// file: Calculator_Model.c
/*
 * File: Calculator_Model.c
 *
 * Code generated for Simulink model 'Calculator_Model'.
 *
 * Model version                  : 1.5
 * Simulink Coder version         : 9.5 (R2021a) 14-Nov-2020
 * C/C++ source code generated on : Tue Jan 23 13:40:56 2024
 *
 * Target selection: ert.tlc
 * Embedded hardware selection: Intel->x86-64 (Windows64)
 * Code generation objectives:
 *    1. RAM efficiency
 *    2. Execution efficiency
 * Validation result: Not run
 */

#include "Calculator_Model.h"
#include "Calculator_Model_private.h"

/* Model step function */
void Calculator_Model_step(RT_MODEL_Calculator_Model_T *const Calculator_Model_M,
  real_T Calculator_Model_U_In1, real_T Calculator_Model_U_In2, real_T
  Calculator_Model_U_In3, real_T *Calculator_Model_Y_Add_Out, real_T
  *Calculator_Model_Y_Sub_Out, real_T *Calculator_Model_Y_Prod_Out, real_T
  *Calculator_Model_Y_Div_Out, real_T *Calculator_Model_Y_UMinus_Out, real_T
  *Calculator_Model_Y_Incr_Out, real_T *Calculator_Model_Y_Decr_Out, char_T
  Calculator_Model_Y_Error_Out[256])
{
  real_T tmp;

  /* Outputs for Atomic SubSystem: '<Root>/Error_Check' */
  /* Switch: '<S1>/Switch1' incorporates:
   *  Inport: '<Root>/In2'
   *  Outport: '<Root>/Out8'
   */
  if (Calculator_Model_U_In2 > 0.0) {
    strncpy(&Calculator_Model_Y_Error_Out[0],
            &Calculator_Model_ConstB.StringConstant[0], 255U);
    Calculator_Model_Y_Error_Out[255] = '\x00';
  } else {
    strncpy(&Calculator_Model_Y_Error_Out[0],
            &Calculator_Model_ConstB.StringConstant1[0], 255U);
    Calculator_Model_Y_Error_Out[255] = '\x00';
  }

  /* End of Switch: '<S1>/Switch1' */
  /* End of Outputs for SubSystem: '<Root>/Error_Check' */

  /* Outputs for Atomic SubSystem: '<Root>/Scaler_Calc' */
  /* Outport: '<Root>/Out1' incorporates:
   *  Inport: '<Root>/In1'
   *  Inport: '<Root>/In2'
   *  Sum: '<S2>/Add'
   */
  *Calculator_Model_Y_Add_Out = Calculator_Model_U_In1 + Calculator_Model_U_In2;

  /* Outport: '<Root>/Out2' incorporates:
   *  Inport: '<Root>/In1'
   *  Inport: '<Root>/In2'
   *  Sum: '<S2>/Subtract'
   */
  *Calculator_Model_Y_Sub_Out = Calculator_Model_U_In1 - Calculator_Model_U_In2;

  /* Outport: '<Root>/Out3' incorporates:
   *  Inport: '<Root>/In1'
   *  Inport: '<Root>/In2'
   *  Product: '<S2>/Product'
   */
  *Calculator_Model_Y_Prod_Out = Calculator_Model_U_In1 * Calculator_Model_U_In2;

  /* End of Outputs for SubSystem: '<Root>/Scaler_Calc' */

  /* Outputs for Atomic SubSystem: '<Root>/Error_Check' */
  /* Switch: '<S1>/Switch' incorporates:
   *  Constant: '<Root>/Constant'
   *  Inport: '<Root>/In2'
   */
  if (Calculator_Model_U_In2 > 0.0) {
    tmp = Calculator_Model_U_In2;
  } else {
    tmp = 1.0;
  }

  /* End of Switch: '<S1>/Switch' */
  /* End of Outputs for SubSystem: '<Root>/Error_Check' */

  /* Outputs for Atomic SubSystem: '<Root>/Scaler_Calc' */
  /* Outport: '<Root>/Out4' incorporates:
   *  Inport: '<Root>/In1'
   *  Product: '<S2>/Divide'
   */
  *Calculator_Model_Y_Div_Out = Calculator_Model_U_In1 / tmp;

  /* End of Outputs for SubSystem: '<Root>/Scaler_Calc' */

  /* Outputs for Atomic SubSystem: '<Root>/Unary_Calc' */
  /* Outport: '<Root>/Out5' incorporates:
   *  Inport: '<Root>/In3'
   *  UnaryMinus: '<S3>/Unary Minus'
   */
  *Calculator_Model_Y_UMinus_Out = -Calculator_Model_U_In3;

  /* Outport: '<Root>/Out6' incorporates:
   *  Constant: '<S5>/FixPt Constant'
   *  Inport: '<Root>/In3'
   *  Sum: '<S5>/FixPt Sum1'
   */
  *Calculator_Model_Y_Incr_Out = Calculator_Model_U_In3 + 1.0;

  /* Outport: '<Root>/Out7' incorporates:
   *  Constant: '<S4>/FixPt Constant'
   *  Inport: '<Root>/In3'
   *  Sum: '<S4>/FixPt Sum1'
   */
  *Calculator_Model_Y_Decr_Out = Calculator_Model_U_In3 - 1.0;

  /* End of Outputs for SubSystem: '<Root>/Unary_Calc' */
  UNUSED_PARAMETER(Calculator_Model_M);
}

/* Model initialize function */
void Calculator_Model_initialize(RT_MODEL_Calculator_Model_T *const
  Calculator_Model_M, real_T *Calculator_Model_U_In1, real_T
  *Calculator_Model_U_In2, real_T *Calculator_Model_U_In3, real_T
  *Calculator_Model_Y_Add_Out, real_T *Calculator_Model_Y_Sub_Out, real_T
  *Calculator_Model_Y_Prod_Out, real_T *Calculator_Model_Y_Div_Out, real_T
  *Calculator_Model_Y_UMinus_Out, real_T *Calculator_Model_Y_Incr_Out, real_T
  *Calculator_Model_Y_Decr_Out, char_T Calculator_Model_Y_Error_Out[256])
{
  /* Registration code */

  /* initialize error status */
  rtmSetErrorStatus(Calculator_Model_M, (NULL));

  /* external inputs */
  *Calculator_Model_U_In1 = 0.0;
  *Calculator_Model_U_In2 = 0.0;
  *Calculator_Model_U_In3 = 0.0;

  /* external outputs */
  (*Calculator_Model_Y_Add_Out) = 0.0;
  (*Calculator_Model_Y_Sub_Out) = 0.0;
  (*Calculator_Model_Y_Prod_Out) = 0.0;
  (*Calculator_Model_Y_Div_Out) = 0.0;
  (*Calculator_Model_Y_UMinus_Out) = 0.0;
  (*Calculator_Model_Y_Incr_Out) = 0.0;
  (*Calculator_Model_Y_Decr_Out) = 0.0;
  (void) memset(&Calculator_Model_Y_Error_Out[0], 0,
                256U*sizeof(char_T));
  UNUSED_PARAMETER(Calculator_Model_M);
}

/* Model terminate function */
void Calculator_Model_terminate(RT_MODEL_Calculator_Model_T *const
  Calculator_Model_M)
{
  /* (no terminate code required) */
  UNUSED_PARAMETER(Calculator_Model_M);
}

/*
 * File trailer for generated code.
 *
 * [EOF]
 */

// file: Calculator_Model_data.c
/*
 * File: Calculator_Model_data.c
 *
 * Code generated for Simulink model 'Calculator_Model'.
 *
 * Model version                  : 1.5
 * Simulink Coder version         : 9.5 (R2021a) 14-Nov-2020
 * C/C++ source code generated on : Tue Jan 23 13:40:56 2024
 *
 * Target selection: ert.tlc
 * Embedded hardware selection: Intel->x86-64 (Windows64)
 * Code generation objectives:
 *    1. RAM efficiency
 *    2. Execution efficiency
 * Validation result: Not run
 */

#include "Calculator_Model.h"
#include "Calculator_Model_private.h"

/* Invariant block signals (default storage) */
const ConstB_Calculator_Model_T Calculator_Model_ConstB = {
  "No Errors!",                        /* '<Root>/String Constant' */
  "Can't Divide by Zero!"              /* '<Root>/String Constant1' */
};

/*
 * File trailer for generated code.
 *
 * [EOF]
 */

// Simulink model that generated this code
simulink model "Calculator_Model"  (R2021a)
settings: Solver=FixedStepDiscrete  StartTime=0.0  StopTime=10.0  RelTol=1e-3
libraries: simulink x2

== system Calculator_Model ==
  In1 : Inport  PortDimensions=1
  In2 : Inport  Port=2  PortDimensions=1
  In3 : Inport  Port=3  PortDimensions=1
  Constant : Constant
  Error_Check : Subsystem  TreatAsAtomicUnit=on
  Scaler_Calc : Subsystem  TreatAsAtomicUnit=on
  String Constant : StringConstant  String="\"No Errors!\""
  String Constant1 : StringConstant  String="\"Can't Divide by Zero!\""
  Unary_Calc : Subsystem  TreatAsAtomicUnit=on
  Out1 : Outport  SignalName=Add_Out
  Out2 : Outport  Port=2  SignalName=Sub_Out
  Out3 : Outport  Port=3  SignalName=Prod_Out
  Out4 : Outport  Port=4  SignalName=Div_Out
  Out5 : Outport  Port=5  SignalName=UMinus_Out
  Out6 : Outport  Port=6  SignalName=Incr_Out
  Out7 : Outport  Port=7  SignalName=Decr_Out
  Out8 : Outport  Port=8  SignalName=Error_Out
  wires:
  In1/1 -> [Num1]
  In3/1 -> [Num3]
  In2/1 -> [Num2]
  [Num1] -> Scaler_Calc/1(In1)
  [Num2] -> Scaler_Calc/2(In2)
  [Num1] -> Scaler_Calc/3(In3)
  [Num2] -> Scaler_Calc/4(In4)
  [Num1] -> Scaler_Calc/5(In5)
  [Num2] -> Scaler_Calc/6(In6)
  [Num1] -> Scaler_Calc/7(In7)
  Scaler_Calc/1(Out1) -> Out1/1
  Scaler_Calc/2(Out2) -> Out2/1
  Scaler_Calc/3(Out3) -> Out3/1
  Scaler_Calc/4(Out4) -> Out4/1
  [Num3] -> Unary_Calc/1(In1)
  [Num3] -> Unary_Calc/2(u)
  [Num3] -> Unary_Calc/3(u1)
  Unary_Calc/1(Out1) -> Out5/1
  Unary_Calc/2(y) -> Out6/1
  Unary_Calc/3(y1) -> Out7/1
  [Num2] -> Error_Check/1(In1)
  Constant/1 -> Error_Check/2(In2)
  String Constant/1 -> Error_Check/3(In3)
  String Constant1/1 -> Error_Check/4(In4)
  Error_Check/1(Out1) -> Scaler_Calc/8(In8)
  Error_Check/2(Out2) -> Out8/1

== system Calculator_Model/Error_Check ==
  In1 : Inport
  In2 : Inport  Port=2
  In3 : Inport  Port=3
  In4 : Inport  Port=4
  Switch : Switch  Criteria=u2 > Threshold
  Switch1 : Switch  Criteria=u2 > Threshold
  Out1 : Outport
  Out2 : Outport  Port=2
  wires:
  Switch/1 -> Out1/1
  In3/1 -> Switch1/1
  In1/1 -> Switch1/2, Switch/2, Switch/1
  Switch1/1 -> Out2/1
  In2/1 -> Switch/3
  In4/1 -> Switch1/3

== system Calculator_Model/Scaler_Calc ==
  In1 : Inport
  In2 : Inport  Port=2
  In3 : Inport  Port=3
  In4 : Inport  Port=4
  In5 : Inport  Port=5
  In6 : Inport  Port=6
  In7 : Inport  Port=7
  In8 : Inport  Port=8
  Add : Sum
  Divide : Product  Inputs=*/
  Product : Product
  Subtract : Sum  Inputs=+-
  Out1 : Outport
  Out2 : Outport  Port=2
  Out3 : Outport  Port=3
  Out4 : Outport  Port=4
  wires:
  Divide/1 -> Out4/1
  In8/1 -> Divide/2
  In7/1 -> Divide/1
  Add/1 -> Out1/1
  In3/1 -> Subtract/1
  In1/1 -> Add/1
  Product/1 -> Out3/1
  In4/1 -> Subtract/2
  In5/1 -> Product/1
  Subtract/1 -> Out2/1
  In2/1 -> Add/2
  In6/1 -> Product/2

== system Calculator_Model/Unary_Calc ==
  In1 : Inport
  u : Inport  Port=2
  u1 : Inport  Port=3
  Decrement Stored Integer : simulink/Additional Math & Discrete/Additional Math: Increment - Decrement/Decrement Stored Integer
  Increment Stored Integer : simulink/Additional Math & Discrete/Additional Math: Increment - Decrement/Increment Stored Integer
  Unary Minus : UnaryMinus
  Out1 : Outport
  y : Outport  Port=2
  y1 : Outport  Port=3
  wires:
  In1/1 -> Unary Minus/1
  Unary Minus/1 -> Out1/1
  Increment Stored Integer/1 -> y/1
  Decrement Stored Integer/1 -> y1/1
  u1/1 -> Decrement Stored Integer/1
  u/1 -> Increment Stored Integer/1
